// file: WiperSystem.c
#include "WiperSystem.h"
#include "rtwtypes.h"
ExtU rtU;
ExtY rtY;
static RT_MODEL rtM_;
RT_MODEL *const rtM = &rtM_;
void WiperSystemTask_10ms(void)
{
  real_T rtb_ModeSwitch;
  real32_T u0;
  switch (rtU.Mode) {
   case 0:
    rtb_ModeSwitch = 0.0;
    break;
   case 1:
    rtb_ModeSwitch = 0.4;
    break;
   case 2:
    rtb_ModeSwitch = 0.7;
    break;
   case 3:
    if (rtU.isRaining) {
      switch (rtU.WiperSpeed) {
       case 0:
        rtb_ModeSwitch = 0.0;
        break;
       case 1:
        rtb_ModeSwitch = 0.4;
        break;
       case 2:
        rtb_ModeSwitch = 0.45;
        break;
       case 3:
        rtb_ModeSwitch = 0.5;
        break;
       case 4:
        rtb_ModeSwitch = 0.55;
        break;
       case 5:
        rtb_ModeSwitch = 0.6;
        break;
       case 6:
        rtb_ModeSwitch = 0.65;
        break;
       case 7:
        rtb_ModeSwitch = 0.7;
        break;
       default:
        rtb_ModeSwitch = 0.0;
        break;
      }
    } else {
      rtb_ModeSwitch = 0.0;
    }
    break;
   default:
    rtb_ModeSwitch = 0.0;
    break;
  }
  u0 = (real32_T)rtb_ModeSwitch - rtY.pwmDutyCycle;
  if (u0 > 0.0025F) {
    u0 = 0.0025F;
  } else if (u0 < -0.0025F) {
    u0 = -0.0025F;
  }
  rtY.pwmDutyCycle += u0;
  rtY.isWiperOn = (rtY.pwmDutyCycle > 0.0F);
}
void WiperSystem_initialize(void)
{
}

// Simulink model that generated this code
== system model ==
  Mode : Inport
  isRaining : Inport
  WiperSpeed : Inport
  WiperSystemTask_10ms : Inport
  pwmDutyCycle : Outport  <- 1: WiperSystem
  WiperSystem : Subsystem  <- 1: Mode, 2: isRaining, 3: WiperSpeed, Trigger: WiperSystemTask_10ms
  isWiperOn : Outport  <- 1: WiperSystem/2
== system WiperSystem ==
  Inport#1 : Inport
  Inport#2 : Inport
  Inport#3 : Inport
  TriggerPort#1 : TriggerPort  TriggerType=function-call
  Outport#1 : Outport  <- 1: Sum#1
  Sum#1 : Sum  Inputs=++  <- 1: Saturate#1, 2: UnitDelay#1
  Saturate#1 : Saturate  UpperLimit=0.0025  LowerLimit=-0.0025  <- 1: Sum#2
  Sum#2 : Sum  Inputs=+-  <- 1: DataTypeConversion#1, 2: UnitDelay#1
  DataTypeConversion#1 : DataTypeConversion  <- 1: ModeSwitch
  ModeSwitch : MultiPortSwitch  DataPortOrder=Zero-based contiguous  Inputs=4  <- 1: Inport#1, 2: Constant#1, 3: Constant#2, 4: Constant#3, 5: Switch#1, 6: Constant#4
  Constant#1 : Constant  Value=0
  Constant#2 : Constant  Value=0.4
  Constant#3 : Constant  Value=0.7
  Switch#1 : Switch  Criteria=u2 ~= 0  <- 1: MultiPortSwitch#1, 2: Inport#2, 3: Constant#5
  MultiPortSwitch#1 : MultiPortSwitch  DataPortOrder=Zero-based contiguous  Inputs=8  <- 1: Inport#3, 2: Constant#6, 3: Constant#7, 4: Constant#8, 5: Constant#9, 6: Constant#10, 7: Constant#11, 8: Constant#12, 9: Constant#13, 10: Constant#14
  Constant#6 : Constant  Value=0
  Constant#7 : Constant  Value=0.4
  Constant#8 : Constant  Value=0.45
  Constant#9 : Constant  Value=0.5
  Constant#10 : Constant  Value=0.55
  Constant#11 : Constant  Value=0.6
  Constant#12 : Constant  Value=0.65
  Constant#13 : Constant  Value=0.7
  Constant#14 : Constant  Value=0
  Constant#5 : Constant  Value=0
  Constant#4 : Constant  Value=0
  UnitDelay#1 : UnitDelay  <- 1: Sum#1
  Outport#2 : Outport  <- 1: CompareToConstant#1
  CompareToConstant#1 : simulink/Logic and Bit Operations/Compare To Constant  relop=>  const=0  <- 1: Sum#1
